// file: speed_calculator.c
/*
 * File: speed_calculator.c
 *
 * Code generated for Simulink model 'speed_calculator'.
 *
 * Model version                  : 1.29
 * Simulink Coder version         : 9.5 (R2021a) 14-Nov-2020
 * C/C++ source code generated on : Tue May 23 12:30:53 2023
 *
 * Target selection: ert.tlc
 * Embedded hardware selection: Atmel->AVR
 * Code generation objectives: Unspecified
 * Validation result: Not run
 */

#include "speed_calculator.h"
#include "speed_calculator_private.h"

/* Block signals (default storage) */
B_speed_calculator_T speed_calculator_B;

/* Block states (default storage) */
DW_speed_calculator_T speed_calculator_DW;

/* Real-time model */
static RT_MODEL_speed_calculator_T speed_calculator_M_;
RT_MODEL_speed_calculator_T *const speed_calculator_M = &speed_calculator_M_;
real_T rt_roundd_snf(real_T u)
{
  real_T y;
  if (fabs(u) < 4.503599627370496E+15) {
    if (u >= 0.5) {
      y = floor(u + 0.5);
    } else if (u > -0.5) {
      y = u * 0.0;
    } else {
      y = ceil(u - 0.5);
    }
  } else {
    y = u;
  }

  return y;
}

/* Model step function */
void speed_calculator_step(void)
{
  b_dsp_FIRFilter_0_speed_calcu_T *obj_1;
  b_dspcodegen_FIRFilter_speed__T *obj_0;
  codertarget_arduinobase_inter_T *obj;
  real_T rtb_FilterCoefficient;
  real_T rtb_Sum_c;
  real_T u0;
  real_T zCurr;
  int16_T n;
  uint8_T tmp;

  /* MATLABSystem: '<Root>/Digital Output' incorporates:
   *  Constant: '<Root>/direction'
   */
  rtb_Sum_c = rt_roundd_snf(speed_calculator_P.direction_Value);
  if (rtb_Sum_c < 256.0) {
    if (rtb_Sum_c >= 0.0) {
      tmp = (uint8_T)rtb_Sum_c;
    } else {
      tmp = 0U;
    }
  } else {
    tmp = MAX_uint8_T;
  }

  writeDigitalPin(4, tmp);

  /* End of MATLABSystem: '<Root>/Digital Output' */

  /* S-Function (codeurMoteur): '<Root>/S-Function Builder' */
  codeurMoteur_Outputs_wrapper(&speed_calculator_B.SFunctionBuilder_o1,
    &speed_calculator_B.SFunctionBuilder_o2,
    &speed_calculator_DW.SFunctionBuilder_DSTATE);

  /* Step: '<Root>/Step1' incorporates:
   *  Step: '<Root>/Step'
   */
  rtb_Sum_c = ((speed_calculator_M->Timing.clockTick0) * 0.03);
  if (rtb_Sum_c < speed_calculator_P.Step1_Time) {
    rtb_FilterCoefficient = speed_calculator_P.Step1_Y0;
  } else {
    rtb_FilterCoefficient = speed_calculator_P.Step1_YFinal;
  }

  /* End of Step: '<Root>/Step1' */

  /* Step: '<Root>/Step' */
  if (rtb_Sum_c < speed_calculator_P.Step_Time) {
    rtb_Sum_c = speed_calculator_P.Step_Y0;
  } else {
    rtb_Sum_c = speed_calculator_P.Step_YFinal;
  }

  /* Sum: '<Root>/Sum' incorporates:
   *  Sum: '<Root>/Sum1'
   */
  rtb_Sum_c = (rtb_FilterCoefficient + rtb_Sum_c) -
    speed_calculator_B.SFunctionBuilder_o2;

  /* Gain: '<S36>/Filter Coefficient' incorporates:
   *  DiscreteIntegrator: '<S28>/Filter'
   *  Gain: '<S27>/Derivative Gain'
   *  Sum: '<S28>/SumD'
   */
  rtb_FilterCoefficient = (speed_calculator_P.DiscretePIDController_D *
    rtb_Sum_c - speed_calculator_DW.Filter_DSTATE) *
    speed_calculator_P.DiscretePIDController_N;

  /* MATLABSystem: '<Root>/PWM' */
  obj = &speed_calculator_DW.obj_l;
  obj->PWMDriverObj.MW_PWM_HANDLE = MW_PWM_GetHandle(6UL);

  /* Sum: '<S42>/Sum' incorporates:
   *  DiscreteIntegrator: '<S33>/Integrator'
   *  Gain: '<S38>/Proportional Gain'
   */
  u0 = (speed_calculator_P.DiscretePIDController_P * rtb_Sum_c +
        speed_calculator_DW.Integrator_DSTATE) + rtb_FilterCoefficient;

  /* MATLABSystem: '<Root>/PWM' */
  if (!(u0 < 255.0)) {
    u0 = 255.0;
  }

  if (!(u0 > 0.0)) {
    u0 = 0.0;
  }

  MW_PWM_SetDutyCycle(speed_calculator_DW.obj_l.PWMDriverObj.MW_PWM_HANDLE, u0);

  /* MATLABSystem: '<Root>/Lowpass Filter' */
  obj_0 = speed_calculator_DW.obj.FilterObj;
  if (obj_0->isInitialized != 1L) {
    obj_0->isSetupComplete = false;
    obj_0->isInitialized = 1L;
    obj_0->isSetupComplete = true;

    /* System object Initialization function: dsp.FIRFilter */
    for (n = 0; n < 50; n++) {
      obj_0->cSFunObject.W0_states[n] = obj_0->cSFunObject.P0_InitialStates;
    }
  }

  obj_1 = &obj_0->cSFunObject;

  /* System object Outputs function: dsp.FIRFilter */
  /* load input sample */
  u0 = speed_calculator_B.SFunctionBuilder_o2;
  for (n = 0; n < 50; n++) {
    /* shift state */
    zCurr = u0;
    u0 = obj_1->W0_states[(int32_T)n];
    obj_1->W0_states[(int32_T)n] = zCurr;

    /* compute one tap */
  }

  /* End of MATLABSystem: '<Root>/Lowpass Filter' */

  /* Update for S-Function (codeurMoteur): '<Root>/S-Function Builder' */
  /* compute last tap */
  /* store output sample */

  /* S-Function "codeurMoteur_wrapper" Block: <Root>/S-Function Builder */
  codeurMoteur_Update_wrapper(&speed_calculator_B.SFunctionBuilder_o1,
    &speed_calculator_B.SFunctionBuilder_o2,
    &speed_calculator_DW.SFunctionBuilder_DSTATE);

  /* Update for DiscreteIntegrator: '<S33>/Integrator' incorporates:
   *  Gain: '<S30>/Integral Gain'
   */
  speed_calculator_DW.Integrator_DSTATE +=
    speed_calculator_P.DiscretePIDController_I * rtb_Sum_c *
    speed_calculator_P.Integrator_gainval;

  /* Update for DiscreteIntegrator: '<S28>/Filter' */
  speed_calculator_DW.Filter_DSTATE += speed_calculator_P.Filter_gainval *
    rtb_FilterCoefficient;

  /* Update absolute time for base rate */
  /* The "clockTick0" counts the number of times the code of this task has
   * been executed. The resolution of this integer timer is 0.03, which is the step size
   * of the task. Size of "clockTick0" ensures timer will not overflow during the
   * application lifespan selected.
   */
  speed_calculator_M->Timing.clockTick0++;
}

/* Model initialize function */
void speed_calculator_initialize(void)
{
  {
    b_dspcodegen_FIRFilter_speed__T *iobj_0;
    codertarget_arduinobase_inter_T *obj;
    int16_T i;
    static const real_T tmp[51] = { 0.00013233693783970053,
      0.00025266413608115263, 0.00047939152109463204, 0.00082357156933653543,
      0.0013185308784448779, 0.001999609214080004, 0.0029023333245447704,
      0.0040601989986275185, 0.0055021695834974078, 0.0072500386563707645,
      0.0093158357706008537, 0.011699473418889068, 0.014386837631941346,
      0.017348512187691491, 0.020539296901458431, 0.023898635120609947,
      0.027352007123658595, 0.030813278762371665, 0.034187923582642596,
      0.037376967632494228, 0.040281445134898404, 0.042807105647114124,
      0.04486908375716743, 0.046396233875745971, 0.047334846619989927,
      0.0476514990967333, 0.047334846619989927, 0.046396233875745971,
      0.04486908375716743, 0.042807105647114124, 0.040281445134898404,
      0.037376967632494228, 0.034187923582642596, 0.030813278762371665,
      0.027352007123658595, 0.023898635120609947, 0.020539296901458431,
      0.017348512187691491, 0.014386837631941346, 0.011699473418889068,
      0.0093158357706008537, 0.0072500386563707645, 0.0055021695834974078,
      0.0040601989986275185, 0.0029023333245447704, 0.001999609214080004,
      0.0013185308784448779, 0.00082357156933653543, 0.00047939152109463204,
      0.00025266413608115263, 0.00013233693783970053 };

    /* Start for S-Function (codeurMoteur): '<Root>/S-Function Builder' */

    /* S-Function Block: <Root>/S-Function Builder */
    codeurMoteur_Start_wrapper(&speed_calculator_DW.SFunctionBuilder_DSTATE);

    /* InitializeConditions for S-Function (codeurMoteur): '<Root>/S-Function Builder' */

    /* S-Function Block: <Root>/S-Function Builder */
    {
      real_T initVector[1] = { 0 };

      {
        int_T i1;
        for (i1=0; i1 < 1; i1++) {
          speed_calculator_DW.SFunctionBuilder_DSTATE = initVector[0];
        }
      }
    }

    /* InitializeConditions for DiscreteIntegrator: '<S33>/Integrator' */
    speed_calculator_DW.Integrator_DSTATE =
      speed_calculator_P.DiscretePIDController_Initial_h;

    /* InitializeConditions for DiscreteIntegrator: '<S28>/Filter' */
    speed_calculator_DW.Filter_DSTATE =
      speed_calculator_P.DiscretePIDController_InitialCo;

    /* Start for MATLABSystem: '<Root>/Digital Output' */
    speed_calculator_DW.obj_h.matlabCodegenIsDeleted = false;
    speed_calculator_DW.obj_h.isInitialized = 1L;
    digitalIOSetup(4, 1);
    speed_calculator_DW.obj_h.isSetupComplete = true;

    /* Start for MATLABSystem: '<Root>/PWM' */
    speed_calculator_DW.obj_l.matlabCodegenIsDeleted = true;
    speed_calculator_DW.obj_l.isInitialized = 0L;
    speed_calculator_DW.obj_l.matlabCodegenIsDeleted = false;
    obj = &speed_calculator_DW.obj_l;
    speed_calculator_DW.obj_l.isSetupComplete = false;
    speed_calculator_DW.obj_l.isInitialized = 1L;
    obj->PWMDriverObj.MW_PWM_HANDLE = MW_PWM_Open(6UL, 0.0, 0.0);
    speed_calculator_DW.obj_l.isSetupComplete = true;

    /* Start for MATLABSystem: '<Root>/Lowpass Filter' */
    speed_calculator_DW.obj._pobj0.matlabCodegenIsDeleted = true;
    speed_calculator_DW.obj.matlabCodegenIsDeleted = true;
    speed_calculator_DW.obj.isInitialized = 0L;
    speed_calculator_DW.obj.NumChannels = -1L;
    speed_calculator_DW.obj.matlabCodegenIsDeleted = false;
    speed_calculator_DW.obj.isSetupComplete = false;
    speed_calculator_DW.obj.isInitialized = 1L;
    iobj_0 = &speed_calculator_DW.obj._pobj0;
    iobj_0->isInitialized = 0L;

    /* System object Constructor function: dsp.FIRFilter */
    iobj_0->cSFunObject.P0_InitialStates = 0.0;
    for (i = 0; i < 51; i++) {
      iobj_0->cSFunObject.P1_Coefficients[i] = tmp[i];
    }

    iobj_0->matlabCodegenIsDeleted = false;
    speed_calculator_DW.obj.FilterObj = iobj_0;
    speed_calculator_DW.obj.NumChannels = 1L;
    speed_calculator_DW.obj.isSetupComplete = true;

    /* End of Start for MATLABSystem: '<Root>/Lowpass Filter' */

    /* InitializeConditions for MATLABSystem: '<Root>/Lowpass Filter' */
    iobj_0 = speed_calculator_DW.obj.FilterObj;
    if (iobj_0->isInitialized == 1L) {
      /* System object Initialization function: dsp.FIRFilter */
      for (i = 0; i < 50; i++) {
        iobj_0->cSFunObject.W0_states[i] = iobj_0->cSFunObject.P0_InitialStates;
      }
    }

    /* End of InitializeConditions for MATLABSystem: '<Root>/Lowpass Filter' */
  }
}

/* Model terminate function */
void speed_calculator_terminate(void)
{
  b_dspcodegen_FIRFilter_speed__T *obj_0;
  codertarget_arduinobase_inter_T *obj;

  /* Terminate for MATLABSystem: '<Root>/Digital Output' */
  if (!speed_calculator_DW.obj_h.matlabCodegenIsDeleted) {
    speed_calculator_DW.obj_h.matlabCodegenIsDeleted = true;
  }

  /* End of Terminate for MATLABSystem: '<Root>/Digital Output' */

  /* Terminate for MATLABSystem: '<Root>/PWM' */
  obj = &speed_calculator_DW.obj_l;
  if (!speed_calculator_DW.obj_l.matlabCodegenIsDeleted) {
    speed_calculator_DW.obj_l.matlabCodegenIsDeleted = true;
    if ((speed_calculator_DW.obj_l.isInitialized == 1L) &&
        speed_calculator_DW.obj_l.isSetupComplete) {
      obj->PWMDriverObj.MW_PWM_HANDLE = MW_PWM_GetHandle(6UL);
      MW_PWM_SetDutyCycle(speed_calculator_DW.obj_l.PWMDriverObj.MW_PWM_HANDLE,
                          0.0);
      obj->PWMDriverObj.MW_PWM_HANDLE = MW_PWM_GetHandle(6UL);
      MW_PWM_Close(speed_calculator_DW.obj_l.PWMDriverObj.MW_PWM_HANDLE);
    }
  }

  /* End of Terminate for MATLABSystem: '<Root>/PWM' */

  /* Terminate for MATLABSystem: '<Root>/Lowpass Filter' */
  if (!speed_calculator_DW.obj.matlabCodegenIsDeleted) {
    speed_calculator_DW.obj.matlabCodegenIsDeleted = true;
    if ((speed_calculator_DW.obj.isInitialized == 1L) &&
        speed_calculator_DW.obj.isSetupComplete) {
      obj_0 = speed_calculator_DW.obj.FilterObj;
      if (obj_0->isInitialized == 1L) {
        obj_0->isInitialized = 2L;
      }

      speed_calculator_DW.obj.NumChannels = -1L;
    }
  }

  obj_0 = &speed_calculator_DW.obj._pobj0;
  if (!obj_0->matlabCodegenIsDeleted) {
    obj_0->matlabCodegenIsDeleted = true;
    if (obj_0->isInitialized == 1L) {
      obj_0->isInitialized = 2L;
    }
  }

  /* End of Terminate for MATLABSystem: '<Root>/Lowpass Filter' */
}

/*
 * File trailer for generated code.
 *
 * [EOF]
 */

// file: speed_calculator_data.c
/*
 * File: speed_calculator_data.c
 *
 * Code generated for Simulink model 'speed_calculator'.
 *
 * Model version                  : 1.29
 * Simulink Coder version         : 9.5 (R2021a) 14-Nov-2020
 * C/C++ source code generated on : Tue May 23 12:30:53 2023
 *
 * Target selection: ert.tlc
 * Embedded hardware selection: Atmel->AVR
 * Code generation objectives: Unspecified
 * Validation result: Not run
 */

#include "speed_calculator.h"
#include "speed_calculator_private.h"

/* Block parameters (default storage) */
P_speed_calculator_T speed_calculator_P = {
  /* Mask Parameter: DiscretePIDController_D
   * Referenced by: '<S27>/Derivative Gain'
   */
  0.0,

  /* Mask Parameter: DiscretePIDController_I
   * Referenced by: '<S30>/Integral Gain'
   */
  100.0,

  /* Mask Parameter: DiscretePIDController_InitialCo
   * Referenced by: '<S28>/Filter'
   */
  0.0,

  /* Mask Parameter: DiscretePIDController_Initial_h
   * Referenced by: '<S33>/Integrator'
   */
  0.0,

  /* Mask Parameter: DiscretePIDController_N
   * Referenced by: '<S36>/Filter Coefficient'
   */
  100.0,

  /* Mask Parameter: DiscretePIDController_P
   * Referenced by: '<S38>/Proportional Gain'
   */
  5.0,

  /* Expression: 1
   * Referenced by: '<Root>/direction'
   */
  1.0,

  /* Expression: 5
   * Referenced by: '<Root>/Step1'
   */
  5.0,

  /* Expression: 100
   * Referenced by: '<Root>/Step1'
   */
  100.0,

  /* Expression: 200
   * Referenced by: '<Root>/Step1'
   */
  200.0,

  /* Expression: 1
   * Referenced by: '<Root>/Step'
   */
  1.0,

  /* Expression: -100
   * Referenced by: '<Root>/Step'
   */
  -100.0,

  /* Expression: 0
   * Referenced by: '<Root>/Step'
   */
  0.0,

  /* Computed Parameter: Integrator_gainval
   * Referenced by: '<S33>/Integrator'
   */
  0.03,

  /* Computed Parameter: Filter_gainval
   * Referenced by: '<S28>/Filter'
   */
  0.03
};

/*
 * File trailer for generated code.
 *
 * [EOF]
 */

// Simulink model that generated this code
simulink model "speed_calculator"  (R2021a)
settings: Solver=FixedStepAuto  StartTime=0.0  StopTime=inf  FixedStep=0.03  RelTol=1e-3  EnableMultiTasking=on
libraries: arduinolib x2, pid_lib x1, dspfdesign x1

== system speed_calculator ==
  Digital Output : arduinolib/Digital Output  pinNumber=4  Direction=output  blockPlatform=arduino
  Discrete PID Controller : pid_lib/PID Controller  Controller=PID  Form=Parallel  TimeDomain=Discrete-time  UseExternalTs=off  SampleTime=0.03  IntegratorMethod=Forward Euler  FilterMethod=Forward Euler  ControllerParametersSource=internal  P=5  I=100  D=0  UseFilter=on  N=100  TunerSelectOption=Transfer Function Based (PID Tuner App)  InitialConditionSource=internal  InitialConditionForIntegrator=0  InitialConditionForFilter=0  DifferentiatorICPrevScaledInput=0  ExternalReset=none  TrackingMode=off  Kt=1  LimitOutput=off  SatLimitsSource=internal  UpperSaturationLimit=inf  LowerSaturationLimit=-inf  LinearizeAsGain=off  AntiWindupMode=none  Kb=1  POutMin=[]  POutMax=[]  IOutMin=[]  IOutMax=[]  DOutMin=[]  DOutMax=[]  NOutMin=[]  NOutMax=[]  SumOutMin=[]  SumOutMax=[]  SaturationOutMin=[]  SaturationOutMax=[]  PParamMin=[]  PParamMax=[]  IParamMin=[]  IParamMax=[]  DParamMin=[]  DParamMax=[]  NParamMin=[]  NParamMax=[]  KbParamMin=[]  KbParamMax=[]  KtParamMin=[]  KtParamMax=[]  KbOutMin=[]  KbOutMax=[]  KtOutMin=[]  KtOutMax=[]  IntegratorOutMin=[]  IntegratorOutMax=[]  FilterOutMin=[]  FilterOutMax=[]  SumI1OutMin=[]  SumI1OutMax=[]  SumI2OutMin=[]  SumI2OutMax=[]  SumI3OutMin=[]  SumI3OutMax=[]  SumI4OutMin=[]  SumI4OutMax=[]  SumDOutMin=[]  SumDOutMax=[]  DifferentiatorOutMin=[]  DifferentiatorOutMax=[]  FilterDiffOutCoefMin=[]  FilterDiffOutCoefMax=[]  ReciprocalOutMin=[]  ReciprocalOutMax=[]  SumDenOutMin=[]  SumDenOutMax=[]  SumNumOutMin=[]  SumNumOutMax=[]  DivideOutMin=[]  DivideOutMax=[]  UdiffTsProdOutMin=[]  UdiffTsProdOutMax=[]  NTsProdOutMin=[]  NTsProdOutMax=[]  UintegralTsProdOutMin=[]  UintegralTsProdOutMax=[]  UngainTsProdOutMin=[]  UngainTsProdOutMax=[]  IntegratorContinuousStateAttributes=''  IntegratorStateMustResolveToSignalObject=off  IntegratorRTWStateStorageClass=Auto  FilterContinuousStateAttributes=''  FilterStateMustResolveToSignalObject=off  FilterRTWStateStorageClass=Auto  ParallelPVariant=InternalParameters  IdealPVariant=Disabled  IVariant=InternalParameters  DVariant=InternalParameters  IntegratorVariant=Discrete  SatVariant=Disabled  AWVariant=Passthrough  PCopyVariant=Disabled  TRVariant=Disabled  FdbkBlocksVariant=Forward  IdealPFdbkVariant=Disabled  SatFdbkVariant=Disabled  DerivativeFilterVariant=ForwardEulerFilter  NVariant=InternalParameters  NCopyVariant=Disabled  FilterICVariant=InternalICsFilter  IntegratorICVariant=InternalICs  ExternalResetVariant=Disabled  TRSumVariant=Passthrough  SumFdbkVariant=Disabled  SumVariant=Sum_PID  TsampFilterVariant=InternalTs  TsampNgainVariant=Passthrough  TsampIntegralVariant=Passthrough  ExternalSaturationOutDataTypeStr=Inherit: Same as second input
  Display1 : Display
  Display2 : Display
  Lowpass Filter : dspfdesign/Lowpass Filter  FilterType=FIR  DesignForMinimumOrder=off  FilterOrder=50  PassbandFrequency=10  StopbandFrequency=10  PassbandRipple=0.1  StopbandAttenuation=80  InheritSampleRate=off  SampleRate=44100  SimulateUsing=Interpreted execution  roundingMode=Floor  coeffsDataTypeStr=fixdt(1,16)
  PWM : arduinolib/PWM  pinNumber=6  frequencyType=Default  desiredFrequency=490.2  achievableFrequency=490.2
  S-Function Builder : S-Function  InitFcn=try, set_param(gcb,'FunctionName','codeurMoteur'), end  FunctionName=codeurMoteur  SFunctionModules=codeurMoteur_wrapper  SFunctionDeploymentMode=off  EnableBusSupport=off  mask(S-Function Builder){}
      mask help: Simulink:masks:SFunctionBuilder_MD
      mask init:
      | val = [[.9  0.75 0.75 1 1 .9 .9 1]',[1 1 0.75 0.75 .9 .9 1 .9]'];try , sys = get_param(gcb,'SfunBuilderFcnName');if isempty(sys), sys = get_param(gcb,'FunctionName'); end,catch, sys = get_param(gcb,'FunctionName'); end
  Scope : Scope  NumInputPorts=2
  Step : Step  Before=-100  After=0  SampleTime=0.03
  Step1 : Step  Time=5  Before=100  After=200  SampleTime=0.03
  Sum : Sum  Inputs=|+-
  Sum1 : Sum  Inputs=++|
  To Workspace : ToWorkspace  VariableName=simout  SaveFormat=Timeseries  SampleTime=0.03
  direction : Constant  SampleTime=0.03
  wires:
  direction/1 -> Digital Output/1
  S-Function Builder/1 -> Display1/1
  Lowpass Filter/1 -> Display2/1, To Workspace/1, Scope/1
  Step1/1 -> Sum1/1
  Step/1 -> Sum1/2
  Discrete PID Controller/1 -> PWM/1
  Sum/1 -> Discrete PID Controller/1
  S-Function Builder/2 -> Sum/2, Lowpass Filter/1
  Sum1/1 -> Scope/2, Sum/1
